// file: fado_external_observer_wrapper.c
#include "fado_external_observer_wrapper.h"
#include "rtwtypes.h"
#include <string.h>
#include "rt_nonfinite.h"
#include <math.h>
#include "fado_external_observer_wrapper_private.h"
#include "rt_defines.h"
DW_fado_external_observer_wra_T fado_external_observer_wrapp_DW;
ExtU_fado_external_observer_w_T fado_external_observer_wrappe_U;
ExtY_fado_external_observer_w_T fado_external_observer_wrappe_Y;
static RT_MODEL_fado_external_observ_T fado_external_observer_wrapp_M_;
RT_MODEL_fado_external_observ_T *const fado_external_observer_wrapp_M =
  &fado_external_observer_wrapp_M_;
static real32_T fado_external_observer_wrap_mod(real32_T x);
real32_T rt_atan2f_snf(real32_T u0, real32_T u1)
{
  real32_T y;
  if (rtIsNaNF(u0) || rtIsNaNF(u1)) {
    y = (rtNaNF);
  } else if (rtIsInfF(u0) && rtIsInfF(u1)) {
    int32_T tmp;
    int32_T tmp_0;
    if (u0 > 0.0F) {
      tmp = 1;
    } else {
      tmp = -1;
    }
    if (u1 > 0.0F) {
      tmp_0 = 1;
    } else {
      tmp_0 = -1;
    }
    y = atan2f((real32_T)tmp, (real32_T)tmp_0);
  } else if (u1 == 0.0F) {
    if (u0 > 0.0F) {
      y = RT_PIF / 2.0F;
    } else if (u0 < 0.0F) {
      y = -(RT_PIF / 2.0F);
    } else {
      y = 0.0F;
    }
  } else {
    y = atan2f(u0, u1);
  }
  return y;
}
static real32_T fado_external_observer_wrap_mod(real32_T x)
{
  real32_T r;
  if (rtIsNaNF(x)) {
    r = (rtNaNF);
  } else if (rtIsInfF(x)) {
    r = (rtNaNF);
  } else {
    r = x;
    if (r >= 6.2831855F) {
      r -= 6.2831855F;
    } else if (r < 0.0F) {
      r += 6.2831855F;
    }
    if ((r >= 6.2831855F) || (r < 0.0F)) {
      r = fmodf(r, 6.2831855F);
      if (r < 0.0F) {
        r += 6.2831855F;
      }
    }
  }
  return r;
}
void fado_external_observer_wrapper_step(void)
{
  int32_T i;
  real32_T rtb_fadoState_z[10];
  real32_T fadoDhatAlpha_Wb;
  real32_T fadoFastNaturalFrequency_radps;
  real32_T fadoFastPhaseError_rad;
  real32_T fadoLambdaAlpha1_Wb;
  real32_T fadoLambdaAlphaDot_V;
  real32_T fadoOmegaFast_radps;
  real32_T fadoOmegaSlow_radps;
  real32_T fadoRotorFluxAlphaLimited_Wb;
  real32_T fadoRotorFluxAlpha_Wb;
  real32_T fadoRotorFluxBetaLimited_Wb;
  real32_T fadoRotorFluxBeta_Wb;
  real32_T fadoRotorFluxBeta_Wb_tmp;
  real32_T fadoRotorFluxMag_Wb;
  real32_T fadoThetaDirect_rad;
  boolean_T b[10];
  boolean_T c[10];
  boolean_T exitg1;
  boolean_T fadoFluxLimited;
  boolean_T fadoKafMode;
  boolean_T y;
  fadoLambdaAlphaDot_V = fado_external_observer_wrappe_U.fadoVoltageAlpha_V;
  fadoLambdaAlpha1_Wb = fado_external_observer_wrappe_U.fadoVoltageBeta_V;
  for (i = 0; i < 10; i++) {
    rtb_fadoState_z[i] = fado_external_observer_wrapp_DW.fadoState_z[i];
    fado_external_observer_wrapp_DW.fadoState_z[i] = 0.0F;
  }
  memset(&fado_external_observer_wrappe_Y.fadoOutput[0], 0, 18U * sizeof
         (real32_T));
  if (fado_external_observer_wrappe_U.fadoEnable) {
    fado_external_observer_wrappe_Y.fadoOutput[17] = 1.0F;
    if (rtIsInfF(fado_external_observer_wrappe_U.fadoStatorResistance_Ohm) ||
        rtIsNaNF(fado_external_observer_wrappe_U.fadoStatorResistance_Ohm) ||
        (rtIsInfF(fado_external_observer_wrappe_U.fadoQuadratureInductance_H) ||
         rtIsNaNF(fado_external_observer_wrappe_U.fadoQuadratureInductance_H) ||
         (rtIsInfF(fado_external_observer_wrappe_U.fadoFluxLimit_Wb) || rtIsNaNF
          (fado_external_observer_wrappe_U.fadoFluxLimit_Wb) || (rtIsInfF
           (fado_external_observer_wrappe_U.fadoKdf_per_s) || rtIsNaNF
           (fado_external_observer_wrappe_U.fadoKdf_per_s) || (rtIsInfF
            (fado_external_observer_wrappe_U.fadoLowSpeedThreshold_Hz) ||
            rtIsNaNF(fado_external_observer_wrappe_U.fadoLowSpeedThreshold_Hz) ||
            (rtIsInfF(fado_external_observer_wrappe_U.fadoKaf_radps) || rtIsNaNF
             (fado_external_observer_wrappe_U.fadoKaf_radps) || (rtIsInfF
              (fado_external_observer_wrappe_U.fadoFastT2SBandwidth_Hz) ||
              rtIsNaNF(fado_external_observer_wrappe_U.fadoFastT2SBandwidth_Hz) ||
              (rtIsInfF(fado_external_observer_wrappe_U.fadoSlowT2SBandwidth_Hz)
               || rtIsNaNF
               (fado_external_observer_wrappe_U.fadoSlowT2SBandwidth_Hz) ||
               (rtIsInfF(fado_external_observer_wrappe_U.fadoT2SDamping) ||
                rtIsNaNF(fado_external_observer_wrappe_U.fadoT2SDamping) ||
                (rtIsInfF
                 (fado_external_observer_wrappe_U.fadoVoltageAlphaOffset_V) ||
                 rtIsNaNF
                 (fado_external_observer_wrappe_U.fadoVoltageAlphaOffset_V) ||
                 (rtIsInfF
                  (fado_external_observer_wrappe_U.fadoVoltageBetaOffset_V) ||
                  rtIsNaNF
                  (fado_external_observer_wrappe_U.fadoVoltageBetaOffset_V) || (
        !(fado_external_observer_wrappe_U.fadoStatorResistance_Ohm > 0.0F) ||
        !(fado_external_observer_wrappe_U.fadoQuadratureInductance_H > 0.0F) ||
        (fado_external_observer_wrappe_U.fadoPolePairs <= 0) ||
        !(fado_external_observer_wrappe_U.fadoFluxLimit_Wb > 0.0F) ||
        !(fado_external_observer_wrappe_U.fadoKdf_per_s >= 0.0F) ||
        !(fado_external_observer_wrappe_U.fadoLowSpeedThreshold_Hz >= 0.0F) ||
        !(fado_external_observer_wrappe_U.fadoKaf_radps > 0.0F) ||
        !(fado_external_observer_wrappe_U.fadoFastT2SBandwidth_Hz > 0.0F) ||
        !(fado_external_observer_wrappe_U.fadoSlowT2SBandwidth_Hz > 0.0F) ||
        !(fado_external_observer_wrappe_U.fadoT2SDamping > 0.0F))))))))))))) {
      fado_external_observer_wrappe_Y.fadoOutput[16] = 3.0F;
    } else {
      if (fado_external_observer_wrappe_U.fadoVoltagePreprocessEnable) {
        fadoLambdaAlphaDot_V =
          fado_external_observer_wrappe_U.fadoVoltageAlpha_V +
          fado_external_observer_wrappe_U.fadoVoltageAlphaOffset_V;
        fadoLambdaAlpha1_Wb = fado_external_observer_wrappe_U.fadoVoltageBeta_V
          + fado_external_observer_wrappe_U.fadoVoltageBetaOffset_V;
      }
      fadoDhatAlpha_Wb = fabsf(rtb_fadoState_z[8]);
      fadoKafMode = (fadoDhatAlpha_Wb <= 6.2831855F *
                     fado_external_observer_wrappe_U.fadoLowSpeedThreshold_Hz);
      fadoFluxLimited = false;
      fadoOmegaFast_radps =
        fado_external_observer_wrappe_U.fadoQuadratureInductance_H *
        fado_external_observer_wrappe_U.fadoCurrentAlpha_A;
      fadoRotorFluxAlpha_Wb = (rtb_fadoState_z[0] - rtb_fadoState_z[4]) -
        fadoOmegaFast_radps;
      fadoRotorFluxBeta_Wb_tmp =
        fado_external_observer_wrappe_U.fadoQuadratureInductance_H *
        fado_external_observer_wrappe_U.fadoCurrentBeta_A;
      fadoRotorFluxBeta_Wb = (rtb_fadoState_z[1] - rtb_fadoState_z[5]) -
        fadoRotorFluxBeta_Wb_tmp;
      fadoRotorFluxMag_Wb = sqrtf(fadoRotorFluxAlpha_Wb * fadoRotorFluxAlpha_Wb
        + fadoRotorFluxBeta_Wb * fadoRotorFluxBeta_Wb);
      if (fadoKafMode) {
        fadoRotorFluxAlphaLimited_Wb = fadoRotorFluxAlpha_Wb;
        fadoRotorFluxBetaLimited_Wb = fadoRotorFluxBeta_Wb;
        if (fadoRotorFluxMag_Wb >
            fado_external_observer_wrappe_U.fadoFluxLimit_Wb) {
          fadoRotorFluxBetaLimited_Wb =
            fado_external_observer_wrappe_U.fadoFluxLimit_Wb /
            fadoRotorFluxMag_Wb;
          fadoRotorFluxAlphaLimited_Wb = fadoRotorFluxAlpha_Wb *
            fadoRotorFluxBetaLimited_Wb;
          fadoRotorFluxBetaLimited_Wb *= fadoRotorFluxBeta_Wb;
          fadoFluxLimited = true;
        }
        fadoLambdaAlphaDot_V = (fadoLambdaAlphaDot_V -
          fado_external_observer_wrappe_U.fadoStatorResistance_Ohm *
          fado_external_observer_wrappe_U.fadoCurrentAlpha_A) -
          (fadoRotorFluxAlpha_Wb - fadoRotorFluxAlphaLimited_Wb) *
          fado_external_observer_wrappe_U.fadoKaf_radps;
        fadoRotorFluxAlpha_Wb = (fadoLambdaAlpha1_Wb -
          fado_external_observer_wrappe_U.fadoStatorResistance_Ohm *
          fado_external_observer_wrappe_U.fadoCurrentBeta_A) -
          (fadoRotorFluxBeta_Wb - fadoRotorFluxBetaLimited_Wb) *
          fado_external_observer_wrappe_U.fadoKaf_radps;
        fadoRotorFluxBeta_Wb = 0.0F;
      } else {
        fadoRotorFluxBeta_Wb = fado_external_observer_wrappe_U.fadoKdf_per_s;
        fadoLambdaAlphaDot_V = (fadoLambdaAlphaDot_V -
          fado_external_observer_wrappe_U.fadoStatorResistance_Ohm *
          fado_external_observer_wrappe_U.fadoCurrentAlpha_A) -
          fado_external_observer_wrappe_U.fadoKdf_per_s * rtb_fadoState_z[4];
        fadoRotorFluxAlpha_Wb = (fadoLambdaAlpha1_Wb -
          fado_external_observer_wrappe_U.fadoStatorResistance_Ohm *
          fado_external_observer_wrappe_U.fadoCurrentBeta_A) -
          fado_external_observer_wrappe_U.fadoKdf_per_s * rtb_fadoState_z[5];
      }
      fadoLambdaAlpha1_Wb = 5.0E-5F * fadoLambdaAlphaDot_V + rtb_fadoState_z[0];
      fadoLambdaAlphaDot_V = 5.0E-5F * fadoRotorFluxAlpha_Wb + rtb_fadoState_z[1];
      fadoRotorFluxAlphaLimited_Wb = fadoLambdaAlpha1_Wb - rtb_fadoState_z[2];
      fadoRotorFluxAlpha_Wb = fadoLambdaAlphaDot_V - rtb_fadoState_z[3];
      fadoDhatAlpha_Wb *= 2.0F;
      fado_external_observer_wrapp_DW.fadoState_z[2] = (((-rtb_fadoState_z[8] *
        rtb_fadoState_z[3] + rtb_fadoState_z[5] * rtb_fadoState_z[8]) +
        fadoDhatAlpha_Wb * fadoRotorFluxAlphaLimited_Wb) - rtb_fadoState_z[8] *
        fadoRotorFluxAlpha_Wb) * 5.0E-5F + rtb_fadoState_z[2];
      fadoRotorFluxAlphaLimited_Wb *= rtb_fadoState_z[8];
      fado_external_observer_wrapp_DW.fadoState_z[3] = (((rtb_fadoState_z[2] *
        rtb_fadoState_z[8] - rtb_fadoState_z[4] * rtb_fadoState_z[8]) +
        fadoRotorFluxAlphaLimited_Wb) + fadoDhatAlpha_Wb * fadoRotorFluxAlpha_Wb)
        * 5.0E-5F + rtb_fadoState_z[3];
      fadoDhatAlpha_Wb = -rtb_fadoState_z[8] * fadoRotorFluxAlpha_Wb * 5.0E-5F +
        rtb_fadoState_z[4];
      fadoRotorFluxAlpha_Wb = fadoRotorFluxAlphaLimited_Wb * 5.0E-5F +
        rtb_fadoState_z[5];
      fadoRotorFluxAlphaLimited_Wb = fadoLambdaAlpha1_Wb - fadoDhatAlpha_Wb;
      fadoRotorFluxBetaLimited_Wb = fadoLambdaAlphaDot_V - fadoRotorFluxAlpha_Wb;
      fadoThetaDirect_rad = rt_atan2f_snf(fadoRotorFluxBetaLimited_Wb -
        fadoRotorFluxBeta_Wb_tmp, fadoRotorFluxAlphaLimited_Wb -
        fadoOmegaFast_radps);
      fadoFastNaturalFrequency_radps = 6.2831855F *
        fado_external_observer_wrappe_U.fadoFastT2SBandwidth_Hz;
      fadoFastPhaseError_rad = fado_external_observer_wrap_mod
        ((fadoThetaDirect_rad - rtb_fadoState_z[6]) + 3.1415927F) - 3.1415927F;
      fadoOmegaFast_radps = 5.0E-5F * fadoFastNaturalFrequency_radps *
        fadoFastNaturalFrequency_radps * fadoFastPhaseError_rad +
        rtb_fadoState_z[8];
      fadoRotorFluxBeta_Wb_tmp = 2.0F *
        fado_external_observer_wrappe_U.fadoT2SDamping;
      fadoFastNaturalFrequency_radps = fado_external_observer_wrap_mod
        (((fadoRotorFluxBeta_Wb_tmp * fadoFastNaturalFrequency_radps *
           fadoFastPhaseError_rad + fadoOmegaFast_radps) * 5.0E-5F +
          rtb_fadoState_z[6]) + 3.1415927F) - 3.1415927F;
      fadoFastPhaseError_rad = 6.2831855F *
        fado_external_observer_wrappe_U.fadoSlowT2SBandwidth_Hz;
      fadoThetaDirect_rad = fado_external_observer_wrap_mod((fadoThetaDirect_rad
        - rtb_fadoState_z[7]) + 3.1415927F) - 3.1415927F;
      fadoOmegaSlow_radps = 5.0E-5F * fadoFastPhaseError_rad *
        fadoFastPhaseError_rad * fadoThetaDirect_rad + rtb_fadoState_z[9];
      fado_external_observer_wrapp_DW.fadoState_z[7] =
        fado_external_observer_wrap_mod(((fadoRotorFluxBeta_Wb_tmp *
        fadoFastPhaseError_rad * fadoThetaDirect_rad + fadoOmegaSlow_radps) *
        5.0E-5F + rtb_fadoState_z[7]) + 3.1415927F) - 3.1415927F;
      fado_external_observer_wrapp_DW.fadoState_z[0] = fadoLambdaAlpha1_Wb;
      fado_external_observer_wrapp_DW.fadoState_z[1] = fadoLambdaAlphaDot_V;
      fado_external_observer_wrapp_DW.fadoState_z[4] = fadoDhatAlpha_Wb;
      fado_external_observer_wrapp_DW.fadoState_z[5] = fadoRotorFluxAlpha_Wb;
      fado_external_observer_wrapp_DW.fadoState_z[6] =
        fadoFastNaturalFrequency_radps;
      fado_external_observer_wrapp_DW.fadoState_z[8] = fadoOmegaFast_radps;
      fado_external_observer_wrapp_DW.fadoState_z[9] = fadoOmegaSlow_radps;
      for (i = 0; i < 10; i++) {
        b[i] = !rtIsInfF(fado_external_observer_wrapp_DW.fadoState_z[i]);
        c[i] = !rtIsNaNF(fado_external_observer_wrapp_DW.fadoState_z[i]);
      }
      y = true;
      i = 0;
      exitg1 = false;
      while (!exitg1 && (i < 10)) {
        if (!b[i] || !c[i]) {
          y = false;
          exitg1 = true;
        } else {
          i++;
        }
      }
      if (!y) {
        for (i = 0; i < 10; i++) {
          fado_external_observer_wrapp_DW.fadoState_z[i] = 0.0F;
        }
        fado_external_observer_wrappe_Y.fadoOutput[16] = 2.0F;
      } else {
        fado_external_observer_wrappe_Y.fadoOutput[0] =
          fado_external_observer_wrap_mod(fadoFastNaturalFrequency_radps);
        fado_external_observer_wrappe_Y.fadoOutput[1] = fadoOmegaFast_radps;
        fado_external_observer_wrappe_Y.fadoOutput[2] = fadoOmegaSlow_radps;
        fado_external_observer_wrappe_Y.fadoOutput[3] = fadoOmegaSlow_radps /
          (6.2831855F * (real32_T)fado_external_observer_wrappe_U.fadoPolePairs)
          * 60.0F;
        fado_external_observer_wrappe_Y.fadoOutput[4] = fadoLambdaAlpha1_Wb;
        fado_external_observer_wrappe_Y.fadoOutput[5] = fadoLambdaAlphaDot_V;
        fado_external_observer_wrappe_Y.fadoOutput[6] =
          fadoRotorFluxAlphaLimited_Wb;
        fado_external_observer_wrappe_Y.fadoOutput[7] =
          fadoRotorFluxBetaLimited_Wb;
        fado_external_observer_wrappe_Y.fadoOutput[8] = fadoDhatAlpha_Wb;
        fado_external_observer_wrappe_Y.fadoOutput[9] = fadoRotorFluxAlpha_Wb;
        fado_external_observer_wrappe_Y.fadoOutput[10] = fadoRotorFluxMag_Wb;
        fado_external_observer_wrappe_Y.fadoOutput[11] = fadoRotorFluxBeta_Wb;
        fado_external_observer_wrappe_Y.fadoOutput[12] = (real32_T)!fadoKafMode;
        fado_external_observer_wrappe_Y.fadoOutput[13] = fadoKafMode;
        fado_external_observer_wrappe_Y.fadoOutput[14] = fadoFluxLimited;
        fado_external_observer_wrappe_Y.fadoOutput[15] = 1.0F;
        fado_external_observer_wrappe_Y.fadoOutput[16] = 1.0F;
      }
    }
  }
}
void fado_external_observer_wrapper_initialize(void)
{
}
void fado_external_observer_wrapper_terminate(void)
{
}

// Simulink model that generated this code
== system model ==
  fadoEnable : Inport
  fadoVoltageAlpha_V : Inport
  fadoVoltageBeta_V : Inport
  fadoCurrentAlpha_A : Inport
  fadoCurrentBeta_A : Inport
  fadoStatorResistance_Ohm : Inport
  fadoQuadratureInductance_H : Inport
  fadoPolePairs : Inport
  fadoFluxLimit_Wb : Inport
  fadoKdf_per_s : Inport
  fadoLowSpeedThreshold_Hz : Inport
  fadoKaf_radps : Inport
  fadoFastT2SBandwidth_Hz : Inport
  fadoSlowT2SBandwidth_Hz : Inport
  fadoT2SDamping : Inport
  fadoVoltageAlphaOffset_V : Inport
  fadoVoltageBetaOffset_V : Inport
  fadoVoltagePreprocessEnable : Inport
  fadoOutput : Outport  <- 1: MATLABFunction#1/2
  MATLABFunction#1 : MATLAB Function  <- 1: fadoEnable, 2: fadoVoltageAlpha_V, 3: fadoVoltageBeta_V, 4: fadoCurrentAlpha_A, 5: fadoCurrentBeta_A, 6: fadoStatorResistance_Ohm, 7: fadoQuadratureInductance_H, 8: fadoPolePairs, 9: fadoFluxLimit_Wb, 10: fadoKdf_per_s, 11: fadoLowSpeedThreshold_Hz, 12: fadoKaf_radps, 13: fadoFastT2SBandwidth_Hz, 14: fadoSlowT2SBandwidth_Hz, 15: fadoT2SDamping, 16: fadoVoltageAlphaOffset_V, 17: fadoVoltageBetaOffset_V, 18: fadoVoltagePreprocessEnable, 19: fadoState_z
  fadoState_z : UnitDelay  InitialCondition=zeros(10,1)  <- 1: MATLABFunction#1
== matlab function MATLABFunction#1 ==
function [fadoStateNext, fadoOutput] = fcn(fadoEnable, fadoVoltageAlpha_V, fadoVoltageBeta_V, fadoCurrentAlpha_A, fadoCurrentBeta_A, fadoStatorResistance_Ohm, fadoQuadratureInductance_H, fadoPolePairs, fadoFluxLimit_Wb, fadoKdf_per_s, fadoLowSpeedThreshold_Hz, fadoKaf_radps, fadoFastT2SBandwidth_Hz, fadoSlowT2SBandwidth_Hz, fadoT2SDamping, fadoVoltageAlphaOffset_V, fadoVoltageBetaOffset_V, fadoVoltagePreprocessEnable, fadoState)
%#codegen
[fadoStateNext, fadoOutput] = fado_external_observer_discrete_update(fadoEnable, fadoVoltageAlpha_V, fadoVoltageBeta_V, fadoCurrentAlpha_A, fadoCurrentBeta_A, fadoStatorResistance_Ohm, fadoQuadratureInductance_H, fadoPolePairs, fadoFluxLimit_Wb, fadoKdf_per_s, fadoLowSpeedThreshold_Hz, fadoKaf_radps, fadoFastT2SBandwidth_Hz, fadoSlowT2SBandwidth_Hz, fadoT2SDamping, fadoVoltageAlphaOffset_V, fadoVoltageBetaOffset_V, fadoVoltagePreprocessEnable, fadoState);
end
